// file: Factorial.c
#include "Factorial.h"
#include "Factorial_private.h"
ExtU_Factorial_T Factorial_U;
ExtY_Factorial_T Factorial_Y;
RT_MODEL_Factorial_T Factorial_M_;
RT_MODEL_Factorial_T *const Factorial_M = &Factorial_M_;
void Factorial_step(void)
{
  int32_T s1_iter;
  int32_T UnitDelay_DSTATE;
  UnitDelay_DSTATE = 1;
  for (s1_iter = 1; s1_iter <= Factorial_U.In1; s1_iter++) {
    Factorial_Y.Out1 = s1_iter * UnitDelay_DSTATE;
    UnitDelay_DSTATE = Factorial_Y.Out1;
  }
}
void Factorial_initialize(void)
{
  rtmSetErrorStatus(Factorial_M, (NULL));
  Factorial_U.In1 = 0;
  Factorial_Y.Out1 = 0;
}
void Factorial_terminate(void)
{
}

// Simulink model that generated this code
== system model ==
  In1 : Inport
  Out1 : Outport  <- 1: Subsystem#1
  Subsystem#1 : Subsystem  <- 1: In1
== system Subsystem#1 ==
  Inport#1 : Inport
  ForIterator#1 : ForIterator  <- 1: Inport#1
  Outport#1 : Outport  <- 1: Product#1
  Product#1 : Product  <- 1: ForIterator#1, 2: UnitDelay
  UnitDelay : UnitDelay  InitialCondition=1  <- 1: Product#1
